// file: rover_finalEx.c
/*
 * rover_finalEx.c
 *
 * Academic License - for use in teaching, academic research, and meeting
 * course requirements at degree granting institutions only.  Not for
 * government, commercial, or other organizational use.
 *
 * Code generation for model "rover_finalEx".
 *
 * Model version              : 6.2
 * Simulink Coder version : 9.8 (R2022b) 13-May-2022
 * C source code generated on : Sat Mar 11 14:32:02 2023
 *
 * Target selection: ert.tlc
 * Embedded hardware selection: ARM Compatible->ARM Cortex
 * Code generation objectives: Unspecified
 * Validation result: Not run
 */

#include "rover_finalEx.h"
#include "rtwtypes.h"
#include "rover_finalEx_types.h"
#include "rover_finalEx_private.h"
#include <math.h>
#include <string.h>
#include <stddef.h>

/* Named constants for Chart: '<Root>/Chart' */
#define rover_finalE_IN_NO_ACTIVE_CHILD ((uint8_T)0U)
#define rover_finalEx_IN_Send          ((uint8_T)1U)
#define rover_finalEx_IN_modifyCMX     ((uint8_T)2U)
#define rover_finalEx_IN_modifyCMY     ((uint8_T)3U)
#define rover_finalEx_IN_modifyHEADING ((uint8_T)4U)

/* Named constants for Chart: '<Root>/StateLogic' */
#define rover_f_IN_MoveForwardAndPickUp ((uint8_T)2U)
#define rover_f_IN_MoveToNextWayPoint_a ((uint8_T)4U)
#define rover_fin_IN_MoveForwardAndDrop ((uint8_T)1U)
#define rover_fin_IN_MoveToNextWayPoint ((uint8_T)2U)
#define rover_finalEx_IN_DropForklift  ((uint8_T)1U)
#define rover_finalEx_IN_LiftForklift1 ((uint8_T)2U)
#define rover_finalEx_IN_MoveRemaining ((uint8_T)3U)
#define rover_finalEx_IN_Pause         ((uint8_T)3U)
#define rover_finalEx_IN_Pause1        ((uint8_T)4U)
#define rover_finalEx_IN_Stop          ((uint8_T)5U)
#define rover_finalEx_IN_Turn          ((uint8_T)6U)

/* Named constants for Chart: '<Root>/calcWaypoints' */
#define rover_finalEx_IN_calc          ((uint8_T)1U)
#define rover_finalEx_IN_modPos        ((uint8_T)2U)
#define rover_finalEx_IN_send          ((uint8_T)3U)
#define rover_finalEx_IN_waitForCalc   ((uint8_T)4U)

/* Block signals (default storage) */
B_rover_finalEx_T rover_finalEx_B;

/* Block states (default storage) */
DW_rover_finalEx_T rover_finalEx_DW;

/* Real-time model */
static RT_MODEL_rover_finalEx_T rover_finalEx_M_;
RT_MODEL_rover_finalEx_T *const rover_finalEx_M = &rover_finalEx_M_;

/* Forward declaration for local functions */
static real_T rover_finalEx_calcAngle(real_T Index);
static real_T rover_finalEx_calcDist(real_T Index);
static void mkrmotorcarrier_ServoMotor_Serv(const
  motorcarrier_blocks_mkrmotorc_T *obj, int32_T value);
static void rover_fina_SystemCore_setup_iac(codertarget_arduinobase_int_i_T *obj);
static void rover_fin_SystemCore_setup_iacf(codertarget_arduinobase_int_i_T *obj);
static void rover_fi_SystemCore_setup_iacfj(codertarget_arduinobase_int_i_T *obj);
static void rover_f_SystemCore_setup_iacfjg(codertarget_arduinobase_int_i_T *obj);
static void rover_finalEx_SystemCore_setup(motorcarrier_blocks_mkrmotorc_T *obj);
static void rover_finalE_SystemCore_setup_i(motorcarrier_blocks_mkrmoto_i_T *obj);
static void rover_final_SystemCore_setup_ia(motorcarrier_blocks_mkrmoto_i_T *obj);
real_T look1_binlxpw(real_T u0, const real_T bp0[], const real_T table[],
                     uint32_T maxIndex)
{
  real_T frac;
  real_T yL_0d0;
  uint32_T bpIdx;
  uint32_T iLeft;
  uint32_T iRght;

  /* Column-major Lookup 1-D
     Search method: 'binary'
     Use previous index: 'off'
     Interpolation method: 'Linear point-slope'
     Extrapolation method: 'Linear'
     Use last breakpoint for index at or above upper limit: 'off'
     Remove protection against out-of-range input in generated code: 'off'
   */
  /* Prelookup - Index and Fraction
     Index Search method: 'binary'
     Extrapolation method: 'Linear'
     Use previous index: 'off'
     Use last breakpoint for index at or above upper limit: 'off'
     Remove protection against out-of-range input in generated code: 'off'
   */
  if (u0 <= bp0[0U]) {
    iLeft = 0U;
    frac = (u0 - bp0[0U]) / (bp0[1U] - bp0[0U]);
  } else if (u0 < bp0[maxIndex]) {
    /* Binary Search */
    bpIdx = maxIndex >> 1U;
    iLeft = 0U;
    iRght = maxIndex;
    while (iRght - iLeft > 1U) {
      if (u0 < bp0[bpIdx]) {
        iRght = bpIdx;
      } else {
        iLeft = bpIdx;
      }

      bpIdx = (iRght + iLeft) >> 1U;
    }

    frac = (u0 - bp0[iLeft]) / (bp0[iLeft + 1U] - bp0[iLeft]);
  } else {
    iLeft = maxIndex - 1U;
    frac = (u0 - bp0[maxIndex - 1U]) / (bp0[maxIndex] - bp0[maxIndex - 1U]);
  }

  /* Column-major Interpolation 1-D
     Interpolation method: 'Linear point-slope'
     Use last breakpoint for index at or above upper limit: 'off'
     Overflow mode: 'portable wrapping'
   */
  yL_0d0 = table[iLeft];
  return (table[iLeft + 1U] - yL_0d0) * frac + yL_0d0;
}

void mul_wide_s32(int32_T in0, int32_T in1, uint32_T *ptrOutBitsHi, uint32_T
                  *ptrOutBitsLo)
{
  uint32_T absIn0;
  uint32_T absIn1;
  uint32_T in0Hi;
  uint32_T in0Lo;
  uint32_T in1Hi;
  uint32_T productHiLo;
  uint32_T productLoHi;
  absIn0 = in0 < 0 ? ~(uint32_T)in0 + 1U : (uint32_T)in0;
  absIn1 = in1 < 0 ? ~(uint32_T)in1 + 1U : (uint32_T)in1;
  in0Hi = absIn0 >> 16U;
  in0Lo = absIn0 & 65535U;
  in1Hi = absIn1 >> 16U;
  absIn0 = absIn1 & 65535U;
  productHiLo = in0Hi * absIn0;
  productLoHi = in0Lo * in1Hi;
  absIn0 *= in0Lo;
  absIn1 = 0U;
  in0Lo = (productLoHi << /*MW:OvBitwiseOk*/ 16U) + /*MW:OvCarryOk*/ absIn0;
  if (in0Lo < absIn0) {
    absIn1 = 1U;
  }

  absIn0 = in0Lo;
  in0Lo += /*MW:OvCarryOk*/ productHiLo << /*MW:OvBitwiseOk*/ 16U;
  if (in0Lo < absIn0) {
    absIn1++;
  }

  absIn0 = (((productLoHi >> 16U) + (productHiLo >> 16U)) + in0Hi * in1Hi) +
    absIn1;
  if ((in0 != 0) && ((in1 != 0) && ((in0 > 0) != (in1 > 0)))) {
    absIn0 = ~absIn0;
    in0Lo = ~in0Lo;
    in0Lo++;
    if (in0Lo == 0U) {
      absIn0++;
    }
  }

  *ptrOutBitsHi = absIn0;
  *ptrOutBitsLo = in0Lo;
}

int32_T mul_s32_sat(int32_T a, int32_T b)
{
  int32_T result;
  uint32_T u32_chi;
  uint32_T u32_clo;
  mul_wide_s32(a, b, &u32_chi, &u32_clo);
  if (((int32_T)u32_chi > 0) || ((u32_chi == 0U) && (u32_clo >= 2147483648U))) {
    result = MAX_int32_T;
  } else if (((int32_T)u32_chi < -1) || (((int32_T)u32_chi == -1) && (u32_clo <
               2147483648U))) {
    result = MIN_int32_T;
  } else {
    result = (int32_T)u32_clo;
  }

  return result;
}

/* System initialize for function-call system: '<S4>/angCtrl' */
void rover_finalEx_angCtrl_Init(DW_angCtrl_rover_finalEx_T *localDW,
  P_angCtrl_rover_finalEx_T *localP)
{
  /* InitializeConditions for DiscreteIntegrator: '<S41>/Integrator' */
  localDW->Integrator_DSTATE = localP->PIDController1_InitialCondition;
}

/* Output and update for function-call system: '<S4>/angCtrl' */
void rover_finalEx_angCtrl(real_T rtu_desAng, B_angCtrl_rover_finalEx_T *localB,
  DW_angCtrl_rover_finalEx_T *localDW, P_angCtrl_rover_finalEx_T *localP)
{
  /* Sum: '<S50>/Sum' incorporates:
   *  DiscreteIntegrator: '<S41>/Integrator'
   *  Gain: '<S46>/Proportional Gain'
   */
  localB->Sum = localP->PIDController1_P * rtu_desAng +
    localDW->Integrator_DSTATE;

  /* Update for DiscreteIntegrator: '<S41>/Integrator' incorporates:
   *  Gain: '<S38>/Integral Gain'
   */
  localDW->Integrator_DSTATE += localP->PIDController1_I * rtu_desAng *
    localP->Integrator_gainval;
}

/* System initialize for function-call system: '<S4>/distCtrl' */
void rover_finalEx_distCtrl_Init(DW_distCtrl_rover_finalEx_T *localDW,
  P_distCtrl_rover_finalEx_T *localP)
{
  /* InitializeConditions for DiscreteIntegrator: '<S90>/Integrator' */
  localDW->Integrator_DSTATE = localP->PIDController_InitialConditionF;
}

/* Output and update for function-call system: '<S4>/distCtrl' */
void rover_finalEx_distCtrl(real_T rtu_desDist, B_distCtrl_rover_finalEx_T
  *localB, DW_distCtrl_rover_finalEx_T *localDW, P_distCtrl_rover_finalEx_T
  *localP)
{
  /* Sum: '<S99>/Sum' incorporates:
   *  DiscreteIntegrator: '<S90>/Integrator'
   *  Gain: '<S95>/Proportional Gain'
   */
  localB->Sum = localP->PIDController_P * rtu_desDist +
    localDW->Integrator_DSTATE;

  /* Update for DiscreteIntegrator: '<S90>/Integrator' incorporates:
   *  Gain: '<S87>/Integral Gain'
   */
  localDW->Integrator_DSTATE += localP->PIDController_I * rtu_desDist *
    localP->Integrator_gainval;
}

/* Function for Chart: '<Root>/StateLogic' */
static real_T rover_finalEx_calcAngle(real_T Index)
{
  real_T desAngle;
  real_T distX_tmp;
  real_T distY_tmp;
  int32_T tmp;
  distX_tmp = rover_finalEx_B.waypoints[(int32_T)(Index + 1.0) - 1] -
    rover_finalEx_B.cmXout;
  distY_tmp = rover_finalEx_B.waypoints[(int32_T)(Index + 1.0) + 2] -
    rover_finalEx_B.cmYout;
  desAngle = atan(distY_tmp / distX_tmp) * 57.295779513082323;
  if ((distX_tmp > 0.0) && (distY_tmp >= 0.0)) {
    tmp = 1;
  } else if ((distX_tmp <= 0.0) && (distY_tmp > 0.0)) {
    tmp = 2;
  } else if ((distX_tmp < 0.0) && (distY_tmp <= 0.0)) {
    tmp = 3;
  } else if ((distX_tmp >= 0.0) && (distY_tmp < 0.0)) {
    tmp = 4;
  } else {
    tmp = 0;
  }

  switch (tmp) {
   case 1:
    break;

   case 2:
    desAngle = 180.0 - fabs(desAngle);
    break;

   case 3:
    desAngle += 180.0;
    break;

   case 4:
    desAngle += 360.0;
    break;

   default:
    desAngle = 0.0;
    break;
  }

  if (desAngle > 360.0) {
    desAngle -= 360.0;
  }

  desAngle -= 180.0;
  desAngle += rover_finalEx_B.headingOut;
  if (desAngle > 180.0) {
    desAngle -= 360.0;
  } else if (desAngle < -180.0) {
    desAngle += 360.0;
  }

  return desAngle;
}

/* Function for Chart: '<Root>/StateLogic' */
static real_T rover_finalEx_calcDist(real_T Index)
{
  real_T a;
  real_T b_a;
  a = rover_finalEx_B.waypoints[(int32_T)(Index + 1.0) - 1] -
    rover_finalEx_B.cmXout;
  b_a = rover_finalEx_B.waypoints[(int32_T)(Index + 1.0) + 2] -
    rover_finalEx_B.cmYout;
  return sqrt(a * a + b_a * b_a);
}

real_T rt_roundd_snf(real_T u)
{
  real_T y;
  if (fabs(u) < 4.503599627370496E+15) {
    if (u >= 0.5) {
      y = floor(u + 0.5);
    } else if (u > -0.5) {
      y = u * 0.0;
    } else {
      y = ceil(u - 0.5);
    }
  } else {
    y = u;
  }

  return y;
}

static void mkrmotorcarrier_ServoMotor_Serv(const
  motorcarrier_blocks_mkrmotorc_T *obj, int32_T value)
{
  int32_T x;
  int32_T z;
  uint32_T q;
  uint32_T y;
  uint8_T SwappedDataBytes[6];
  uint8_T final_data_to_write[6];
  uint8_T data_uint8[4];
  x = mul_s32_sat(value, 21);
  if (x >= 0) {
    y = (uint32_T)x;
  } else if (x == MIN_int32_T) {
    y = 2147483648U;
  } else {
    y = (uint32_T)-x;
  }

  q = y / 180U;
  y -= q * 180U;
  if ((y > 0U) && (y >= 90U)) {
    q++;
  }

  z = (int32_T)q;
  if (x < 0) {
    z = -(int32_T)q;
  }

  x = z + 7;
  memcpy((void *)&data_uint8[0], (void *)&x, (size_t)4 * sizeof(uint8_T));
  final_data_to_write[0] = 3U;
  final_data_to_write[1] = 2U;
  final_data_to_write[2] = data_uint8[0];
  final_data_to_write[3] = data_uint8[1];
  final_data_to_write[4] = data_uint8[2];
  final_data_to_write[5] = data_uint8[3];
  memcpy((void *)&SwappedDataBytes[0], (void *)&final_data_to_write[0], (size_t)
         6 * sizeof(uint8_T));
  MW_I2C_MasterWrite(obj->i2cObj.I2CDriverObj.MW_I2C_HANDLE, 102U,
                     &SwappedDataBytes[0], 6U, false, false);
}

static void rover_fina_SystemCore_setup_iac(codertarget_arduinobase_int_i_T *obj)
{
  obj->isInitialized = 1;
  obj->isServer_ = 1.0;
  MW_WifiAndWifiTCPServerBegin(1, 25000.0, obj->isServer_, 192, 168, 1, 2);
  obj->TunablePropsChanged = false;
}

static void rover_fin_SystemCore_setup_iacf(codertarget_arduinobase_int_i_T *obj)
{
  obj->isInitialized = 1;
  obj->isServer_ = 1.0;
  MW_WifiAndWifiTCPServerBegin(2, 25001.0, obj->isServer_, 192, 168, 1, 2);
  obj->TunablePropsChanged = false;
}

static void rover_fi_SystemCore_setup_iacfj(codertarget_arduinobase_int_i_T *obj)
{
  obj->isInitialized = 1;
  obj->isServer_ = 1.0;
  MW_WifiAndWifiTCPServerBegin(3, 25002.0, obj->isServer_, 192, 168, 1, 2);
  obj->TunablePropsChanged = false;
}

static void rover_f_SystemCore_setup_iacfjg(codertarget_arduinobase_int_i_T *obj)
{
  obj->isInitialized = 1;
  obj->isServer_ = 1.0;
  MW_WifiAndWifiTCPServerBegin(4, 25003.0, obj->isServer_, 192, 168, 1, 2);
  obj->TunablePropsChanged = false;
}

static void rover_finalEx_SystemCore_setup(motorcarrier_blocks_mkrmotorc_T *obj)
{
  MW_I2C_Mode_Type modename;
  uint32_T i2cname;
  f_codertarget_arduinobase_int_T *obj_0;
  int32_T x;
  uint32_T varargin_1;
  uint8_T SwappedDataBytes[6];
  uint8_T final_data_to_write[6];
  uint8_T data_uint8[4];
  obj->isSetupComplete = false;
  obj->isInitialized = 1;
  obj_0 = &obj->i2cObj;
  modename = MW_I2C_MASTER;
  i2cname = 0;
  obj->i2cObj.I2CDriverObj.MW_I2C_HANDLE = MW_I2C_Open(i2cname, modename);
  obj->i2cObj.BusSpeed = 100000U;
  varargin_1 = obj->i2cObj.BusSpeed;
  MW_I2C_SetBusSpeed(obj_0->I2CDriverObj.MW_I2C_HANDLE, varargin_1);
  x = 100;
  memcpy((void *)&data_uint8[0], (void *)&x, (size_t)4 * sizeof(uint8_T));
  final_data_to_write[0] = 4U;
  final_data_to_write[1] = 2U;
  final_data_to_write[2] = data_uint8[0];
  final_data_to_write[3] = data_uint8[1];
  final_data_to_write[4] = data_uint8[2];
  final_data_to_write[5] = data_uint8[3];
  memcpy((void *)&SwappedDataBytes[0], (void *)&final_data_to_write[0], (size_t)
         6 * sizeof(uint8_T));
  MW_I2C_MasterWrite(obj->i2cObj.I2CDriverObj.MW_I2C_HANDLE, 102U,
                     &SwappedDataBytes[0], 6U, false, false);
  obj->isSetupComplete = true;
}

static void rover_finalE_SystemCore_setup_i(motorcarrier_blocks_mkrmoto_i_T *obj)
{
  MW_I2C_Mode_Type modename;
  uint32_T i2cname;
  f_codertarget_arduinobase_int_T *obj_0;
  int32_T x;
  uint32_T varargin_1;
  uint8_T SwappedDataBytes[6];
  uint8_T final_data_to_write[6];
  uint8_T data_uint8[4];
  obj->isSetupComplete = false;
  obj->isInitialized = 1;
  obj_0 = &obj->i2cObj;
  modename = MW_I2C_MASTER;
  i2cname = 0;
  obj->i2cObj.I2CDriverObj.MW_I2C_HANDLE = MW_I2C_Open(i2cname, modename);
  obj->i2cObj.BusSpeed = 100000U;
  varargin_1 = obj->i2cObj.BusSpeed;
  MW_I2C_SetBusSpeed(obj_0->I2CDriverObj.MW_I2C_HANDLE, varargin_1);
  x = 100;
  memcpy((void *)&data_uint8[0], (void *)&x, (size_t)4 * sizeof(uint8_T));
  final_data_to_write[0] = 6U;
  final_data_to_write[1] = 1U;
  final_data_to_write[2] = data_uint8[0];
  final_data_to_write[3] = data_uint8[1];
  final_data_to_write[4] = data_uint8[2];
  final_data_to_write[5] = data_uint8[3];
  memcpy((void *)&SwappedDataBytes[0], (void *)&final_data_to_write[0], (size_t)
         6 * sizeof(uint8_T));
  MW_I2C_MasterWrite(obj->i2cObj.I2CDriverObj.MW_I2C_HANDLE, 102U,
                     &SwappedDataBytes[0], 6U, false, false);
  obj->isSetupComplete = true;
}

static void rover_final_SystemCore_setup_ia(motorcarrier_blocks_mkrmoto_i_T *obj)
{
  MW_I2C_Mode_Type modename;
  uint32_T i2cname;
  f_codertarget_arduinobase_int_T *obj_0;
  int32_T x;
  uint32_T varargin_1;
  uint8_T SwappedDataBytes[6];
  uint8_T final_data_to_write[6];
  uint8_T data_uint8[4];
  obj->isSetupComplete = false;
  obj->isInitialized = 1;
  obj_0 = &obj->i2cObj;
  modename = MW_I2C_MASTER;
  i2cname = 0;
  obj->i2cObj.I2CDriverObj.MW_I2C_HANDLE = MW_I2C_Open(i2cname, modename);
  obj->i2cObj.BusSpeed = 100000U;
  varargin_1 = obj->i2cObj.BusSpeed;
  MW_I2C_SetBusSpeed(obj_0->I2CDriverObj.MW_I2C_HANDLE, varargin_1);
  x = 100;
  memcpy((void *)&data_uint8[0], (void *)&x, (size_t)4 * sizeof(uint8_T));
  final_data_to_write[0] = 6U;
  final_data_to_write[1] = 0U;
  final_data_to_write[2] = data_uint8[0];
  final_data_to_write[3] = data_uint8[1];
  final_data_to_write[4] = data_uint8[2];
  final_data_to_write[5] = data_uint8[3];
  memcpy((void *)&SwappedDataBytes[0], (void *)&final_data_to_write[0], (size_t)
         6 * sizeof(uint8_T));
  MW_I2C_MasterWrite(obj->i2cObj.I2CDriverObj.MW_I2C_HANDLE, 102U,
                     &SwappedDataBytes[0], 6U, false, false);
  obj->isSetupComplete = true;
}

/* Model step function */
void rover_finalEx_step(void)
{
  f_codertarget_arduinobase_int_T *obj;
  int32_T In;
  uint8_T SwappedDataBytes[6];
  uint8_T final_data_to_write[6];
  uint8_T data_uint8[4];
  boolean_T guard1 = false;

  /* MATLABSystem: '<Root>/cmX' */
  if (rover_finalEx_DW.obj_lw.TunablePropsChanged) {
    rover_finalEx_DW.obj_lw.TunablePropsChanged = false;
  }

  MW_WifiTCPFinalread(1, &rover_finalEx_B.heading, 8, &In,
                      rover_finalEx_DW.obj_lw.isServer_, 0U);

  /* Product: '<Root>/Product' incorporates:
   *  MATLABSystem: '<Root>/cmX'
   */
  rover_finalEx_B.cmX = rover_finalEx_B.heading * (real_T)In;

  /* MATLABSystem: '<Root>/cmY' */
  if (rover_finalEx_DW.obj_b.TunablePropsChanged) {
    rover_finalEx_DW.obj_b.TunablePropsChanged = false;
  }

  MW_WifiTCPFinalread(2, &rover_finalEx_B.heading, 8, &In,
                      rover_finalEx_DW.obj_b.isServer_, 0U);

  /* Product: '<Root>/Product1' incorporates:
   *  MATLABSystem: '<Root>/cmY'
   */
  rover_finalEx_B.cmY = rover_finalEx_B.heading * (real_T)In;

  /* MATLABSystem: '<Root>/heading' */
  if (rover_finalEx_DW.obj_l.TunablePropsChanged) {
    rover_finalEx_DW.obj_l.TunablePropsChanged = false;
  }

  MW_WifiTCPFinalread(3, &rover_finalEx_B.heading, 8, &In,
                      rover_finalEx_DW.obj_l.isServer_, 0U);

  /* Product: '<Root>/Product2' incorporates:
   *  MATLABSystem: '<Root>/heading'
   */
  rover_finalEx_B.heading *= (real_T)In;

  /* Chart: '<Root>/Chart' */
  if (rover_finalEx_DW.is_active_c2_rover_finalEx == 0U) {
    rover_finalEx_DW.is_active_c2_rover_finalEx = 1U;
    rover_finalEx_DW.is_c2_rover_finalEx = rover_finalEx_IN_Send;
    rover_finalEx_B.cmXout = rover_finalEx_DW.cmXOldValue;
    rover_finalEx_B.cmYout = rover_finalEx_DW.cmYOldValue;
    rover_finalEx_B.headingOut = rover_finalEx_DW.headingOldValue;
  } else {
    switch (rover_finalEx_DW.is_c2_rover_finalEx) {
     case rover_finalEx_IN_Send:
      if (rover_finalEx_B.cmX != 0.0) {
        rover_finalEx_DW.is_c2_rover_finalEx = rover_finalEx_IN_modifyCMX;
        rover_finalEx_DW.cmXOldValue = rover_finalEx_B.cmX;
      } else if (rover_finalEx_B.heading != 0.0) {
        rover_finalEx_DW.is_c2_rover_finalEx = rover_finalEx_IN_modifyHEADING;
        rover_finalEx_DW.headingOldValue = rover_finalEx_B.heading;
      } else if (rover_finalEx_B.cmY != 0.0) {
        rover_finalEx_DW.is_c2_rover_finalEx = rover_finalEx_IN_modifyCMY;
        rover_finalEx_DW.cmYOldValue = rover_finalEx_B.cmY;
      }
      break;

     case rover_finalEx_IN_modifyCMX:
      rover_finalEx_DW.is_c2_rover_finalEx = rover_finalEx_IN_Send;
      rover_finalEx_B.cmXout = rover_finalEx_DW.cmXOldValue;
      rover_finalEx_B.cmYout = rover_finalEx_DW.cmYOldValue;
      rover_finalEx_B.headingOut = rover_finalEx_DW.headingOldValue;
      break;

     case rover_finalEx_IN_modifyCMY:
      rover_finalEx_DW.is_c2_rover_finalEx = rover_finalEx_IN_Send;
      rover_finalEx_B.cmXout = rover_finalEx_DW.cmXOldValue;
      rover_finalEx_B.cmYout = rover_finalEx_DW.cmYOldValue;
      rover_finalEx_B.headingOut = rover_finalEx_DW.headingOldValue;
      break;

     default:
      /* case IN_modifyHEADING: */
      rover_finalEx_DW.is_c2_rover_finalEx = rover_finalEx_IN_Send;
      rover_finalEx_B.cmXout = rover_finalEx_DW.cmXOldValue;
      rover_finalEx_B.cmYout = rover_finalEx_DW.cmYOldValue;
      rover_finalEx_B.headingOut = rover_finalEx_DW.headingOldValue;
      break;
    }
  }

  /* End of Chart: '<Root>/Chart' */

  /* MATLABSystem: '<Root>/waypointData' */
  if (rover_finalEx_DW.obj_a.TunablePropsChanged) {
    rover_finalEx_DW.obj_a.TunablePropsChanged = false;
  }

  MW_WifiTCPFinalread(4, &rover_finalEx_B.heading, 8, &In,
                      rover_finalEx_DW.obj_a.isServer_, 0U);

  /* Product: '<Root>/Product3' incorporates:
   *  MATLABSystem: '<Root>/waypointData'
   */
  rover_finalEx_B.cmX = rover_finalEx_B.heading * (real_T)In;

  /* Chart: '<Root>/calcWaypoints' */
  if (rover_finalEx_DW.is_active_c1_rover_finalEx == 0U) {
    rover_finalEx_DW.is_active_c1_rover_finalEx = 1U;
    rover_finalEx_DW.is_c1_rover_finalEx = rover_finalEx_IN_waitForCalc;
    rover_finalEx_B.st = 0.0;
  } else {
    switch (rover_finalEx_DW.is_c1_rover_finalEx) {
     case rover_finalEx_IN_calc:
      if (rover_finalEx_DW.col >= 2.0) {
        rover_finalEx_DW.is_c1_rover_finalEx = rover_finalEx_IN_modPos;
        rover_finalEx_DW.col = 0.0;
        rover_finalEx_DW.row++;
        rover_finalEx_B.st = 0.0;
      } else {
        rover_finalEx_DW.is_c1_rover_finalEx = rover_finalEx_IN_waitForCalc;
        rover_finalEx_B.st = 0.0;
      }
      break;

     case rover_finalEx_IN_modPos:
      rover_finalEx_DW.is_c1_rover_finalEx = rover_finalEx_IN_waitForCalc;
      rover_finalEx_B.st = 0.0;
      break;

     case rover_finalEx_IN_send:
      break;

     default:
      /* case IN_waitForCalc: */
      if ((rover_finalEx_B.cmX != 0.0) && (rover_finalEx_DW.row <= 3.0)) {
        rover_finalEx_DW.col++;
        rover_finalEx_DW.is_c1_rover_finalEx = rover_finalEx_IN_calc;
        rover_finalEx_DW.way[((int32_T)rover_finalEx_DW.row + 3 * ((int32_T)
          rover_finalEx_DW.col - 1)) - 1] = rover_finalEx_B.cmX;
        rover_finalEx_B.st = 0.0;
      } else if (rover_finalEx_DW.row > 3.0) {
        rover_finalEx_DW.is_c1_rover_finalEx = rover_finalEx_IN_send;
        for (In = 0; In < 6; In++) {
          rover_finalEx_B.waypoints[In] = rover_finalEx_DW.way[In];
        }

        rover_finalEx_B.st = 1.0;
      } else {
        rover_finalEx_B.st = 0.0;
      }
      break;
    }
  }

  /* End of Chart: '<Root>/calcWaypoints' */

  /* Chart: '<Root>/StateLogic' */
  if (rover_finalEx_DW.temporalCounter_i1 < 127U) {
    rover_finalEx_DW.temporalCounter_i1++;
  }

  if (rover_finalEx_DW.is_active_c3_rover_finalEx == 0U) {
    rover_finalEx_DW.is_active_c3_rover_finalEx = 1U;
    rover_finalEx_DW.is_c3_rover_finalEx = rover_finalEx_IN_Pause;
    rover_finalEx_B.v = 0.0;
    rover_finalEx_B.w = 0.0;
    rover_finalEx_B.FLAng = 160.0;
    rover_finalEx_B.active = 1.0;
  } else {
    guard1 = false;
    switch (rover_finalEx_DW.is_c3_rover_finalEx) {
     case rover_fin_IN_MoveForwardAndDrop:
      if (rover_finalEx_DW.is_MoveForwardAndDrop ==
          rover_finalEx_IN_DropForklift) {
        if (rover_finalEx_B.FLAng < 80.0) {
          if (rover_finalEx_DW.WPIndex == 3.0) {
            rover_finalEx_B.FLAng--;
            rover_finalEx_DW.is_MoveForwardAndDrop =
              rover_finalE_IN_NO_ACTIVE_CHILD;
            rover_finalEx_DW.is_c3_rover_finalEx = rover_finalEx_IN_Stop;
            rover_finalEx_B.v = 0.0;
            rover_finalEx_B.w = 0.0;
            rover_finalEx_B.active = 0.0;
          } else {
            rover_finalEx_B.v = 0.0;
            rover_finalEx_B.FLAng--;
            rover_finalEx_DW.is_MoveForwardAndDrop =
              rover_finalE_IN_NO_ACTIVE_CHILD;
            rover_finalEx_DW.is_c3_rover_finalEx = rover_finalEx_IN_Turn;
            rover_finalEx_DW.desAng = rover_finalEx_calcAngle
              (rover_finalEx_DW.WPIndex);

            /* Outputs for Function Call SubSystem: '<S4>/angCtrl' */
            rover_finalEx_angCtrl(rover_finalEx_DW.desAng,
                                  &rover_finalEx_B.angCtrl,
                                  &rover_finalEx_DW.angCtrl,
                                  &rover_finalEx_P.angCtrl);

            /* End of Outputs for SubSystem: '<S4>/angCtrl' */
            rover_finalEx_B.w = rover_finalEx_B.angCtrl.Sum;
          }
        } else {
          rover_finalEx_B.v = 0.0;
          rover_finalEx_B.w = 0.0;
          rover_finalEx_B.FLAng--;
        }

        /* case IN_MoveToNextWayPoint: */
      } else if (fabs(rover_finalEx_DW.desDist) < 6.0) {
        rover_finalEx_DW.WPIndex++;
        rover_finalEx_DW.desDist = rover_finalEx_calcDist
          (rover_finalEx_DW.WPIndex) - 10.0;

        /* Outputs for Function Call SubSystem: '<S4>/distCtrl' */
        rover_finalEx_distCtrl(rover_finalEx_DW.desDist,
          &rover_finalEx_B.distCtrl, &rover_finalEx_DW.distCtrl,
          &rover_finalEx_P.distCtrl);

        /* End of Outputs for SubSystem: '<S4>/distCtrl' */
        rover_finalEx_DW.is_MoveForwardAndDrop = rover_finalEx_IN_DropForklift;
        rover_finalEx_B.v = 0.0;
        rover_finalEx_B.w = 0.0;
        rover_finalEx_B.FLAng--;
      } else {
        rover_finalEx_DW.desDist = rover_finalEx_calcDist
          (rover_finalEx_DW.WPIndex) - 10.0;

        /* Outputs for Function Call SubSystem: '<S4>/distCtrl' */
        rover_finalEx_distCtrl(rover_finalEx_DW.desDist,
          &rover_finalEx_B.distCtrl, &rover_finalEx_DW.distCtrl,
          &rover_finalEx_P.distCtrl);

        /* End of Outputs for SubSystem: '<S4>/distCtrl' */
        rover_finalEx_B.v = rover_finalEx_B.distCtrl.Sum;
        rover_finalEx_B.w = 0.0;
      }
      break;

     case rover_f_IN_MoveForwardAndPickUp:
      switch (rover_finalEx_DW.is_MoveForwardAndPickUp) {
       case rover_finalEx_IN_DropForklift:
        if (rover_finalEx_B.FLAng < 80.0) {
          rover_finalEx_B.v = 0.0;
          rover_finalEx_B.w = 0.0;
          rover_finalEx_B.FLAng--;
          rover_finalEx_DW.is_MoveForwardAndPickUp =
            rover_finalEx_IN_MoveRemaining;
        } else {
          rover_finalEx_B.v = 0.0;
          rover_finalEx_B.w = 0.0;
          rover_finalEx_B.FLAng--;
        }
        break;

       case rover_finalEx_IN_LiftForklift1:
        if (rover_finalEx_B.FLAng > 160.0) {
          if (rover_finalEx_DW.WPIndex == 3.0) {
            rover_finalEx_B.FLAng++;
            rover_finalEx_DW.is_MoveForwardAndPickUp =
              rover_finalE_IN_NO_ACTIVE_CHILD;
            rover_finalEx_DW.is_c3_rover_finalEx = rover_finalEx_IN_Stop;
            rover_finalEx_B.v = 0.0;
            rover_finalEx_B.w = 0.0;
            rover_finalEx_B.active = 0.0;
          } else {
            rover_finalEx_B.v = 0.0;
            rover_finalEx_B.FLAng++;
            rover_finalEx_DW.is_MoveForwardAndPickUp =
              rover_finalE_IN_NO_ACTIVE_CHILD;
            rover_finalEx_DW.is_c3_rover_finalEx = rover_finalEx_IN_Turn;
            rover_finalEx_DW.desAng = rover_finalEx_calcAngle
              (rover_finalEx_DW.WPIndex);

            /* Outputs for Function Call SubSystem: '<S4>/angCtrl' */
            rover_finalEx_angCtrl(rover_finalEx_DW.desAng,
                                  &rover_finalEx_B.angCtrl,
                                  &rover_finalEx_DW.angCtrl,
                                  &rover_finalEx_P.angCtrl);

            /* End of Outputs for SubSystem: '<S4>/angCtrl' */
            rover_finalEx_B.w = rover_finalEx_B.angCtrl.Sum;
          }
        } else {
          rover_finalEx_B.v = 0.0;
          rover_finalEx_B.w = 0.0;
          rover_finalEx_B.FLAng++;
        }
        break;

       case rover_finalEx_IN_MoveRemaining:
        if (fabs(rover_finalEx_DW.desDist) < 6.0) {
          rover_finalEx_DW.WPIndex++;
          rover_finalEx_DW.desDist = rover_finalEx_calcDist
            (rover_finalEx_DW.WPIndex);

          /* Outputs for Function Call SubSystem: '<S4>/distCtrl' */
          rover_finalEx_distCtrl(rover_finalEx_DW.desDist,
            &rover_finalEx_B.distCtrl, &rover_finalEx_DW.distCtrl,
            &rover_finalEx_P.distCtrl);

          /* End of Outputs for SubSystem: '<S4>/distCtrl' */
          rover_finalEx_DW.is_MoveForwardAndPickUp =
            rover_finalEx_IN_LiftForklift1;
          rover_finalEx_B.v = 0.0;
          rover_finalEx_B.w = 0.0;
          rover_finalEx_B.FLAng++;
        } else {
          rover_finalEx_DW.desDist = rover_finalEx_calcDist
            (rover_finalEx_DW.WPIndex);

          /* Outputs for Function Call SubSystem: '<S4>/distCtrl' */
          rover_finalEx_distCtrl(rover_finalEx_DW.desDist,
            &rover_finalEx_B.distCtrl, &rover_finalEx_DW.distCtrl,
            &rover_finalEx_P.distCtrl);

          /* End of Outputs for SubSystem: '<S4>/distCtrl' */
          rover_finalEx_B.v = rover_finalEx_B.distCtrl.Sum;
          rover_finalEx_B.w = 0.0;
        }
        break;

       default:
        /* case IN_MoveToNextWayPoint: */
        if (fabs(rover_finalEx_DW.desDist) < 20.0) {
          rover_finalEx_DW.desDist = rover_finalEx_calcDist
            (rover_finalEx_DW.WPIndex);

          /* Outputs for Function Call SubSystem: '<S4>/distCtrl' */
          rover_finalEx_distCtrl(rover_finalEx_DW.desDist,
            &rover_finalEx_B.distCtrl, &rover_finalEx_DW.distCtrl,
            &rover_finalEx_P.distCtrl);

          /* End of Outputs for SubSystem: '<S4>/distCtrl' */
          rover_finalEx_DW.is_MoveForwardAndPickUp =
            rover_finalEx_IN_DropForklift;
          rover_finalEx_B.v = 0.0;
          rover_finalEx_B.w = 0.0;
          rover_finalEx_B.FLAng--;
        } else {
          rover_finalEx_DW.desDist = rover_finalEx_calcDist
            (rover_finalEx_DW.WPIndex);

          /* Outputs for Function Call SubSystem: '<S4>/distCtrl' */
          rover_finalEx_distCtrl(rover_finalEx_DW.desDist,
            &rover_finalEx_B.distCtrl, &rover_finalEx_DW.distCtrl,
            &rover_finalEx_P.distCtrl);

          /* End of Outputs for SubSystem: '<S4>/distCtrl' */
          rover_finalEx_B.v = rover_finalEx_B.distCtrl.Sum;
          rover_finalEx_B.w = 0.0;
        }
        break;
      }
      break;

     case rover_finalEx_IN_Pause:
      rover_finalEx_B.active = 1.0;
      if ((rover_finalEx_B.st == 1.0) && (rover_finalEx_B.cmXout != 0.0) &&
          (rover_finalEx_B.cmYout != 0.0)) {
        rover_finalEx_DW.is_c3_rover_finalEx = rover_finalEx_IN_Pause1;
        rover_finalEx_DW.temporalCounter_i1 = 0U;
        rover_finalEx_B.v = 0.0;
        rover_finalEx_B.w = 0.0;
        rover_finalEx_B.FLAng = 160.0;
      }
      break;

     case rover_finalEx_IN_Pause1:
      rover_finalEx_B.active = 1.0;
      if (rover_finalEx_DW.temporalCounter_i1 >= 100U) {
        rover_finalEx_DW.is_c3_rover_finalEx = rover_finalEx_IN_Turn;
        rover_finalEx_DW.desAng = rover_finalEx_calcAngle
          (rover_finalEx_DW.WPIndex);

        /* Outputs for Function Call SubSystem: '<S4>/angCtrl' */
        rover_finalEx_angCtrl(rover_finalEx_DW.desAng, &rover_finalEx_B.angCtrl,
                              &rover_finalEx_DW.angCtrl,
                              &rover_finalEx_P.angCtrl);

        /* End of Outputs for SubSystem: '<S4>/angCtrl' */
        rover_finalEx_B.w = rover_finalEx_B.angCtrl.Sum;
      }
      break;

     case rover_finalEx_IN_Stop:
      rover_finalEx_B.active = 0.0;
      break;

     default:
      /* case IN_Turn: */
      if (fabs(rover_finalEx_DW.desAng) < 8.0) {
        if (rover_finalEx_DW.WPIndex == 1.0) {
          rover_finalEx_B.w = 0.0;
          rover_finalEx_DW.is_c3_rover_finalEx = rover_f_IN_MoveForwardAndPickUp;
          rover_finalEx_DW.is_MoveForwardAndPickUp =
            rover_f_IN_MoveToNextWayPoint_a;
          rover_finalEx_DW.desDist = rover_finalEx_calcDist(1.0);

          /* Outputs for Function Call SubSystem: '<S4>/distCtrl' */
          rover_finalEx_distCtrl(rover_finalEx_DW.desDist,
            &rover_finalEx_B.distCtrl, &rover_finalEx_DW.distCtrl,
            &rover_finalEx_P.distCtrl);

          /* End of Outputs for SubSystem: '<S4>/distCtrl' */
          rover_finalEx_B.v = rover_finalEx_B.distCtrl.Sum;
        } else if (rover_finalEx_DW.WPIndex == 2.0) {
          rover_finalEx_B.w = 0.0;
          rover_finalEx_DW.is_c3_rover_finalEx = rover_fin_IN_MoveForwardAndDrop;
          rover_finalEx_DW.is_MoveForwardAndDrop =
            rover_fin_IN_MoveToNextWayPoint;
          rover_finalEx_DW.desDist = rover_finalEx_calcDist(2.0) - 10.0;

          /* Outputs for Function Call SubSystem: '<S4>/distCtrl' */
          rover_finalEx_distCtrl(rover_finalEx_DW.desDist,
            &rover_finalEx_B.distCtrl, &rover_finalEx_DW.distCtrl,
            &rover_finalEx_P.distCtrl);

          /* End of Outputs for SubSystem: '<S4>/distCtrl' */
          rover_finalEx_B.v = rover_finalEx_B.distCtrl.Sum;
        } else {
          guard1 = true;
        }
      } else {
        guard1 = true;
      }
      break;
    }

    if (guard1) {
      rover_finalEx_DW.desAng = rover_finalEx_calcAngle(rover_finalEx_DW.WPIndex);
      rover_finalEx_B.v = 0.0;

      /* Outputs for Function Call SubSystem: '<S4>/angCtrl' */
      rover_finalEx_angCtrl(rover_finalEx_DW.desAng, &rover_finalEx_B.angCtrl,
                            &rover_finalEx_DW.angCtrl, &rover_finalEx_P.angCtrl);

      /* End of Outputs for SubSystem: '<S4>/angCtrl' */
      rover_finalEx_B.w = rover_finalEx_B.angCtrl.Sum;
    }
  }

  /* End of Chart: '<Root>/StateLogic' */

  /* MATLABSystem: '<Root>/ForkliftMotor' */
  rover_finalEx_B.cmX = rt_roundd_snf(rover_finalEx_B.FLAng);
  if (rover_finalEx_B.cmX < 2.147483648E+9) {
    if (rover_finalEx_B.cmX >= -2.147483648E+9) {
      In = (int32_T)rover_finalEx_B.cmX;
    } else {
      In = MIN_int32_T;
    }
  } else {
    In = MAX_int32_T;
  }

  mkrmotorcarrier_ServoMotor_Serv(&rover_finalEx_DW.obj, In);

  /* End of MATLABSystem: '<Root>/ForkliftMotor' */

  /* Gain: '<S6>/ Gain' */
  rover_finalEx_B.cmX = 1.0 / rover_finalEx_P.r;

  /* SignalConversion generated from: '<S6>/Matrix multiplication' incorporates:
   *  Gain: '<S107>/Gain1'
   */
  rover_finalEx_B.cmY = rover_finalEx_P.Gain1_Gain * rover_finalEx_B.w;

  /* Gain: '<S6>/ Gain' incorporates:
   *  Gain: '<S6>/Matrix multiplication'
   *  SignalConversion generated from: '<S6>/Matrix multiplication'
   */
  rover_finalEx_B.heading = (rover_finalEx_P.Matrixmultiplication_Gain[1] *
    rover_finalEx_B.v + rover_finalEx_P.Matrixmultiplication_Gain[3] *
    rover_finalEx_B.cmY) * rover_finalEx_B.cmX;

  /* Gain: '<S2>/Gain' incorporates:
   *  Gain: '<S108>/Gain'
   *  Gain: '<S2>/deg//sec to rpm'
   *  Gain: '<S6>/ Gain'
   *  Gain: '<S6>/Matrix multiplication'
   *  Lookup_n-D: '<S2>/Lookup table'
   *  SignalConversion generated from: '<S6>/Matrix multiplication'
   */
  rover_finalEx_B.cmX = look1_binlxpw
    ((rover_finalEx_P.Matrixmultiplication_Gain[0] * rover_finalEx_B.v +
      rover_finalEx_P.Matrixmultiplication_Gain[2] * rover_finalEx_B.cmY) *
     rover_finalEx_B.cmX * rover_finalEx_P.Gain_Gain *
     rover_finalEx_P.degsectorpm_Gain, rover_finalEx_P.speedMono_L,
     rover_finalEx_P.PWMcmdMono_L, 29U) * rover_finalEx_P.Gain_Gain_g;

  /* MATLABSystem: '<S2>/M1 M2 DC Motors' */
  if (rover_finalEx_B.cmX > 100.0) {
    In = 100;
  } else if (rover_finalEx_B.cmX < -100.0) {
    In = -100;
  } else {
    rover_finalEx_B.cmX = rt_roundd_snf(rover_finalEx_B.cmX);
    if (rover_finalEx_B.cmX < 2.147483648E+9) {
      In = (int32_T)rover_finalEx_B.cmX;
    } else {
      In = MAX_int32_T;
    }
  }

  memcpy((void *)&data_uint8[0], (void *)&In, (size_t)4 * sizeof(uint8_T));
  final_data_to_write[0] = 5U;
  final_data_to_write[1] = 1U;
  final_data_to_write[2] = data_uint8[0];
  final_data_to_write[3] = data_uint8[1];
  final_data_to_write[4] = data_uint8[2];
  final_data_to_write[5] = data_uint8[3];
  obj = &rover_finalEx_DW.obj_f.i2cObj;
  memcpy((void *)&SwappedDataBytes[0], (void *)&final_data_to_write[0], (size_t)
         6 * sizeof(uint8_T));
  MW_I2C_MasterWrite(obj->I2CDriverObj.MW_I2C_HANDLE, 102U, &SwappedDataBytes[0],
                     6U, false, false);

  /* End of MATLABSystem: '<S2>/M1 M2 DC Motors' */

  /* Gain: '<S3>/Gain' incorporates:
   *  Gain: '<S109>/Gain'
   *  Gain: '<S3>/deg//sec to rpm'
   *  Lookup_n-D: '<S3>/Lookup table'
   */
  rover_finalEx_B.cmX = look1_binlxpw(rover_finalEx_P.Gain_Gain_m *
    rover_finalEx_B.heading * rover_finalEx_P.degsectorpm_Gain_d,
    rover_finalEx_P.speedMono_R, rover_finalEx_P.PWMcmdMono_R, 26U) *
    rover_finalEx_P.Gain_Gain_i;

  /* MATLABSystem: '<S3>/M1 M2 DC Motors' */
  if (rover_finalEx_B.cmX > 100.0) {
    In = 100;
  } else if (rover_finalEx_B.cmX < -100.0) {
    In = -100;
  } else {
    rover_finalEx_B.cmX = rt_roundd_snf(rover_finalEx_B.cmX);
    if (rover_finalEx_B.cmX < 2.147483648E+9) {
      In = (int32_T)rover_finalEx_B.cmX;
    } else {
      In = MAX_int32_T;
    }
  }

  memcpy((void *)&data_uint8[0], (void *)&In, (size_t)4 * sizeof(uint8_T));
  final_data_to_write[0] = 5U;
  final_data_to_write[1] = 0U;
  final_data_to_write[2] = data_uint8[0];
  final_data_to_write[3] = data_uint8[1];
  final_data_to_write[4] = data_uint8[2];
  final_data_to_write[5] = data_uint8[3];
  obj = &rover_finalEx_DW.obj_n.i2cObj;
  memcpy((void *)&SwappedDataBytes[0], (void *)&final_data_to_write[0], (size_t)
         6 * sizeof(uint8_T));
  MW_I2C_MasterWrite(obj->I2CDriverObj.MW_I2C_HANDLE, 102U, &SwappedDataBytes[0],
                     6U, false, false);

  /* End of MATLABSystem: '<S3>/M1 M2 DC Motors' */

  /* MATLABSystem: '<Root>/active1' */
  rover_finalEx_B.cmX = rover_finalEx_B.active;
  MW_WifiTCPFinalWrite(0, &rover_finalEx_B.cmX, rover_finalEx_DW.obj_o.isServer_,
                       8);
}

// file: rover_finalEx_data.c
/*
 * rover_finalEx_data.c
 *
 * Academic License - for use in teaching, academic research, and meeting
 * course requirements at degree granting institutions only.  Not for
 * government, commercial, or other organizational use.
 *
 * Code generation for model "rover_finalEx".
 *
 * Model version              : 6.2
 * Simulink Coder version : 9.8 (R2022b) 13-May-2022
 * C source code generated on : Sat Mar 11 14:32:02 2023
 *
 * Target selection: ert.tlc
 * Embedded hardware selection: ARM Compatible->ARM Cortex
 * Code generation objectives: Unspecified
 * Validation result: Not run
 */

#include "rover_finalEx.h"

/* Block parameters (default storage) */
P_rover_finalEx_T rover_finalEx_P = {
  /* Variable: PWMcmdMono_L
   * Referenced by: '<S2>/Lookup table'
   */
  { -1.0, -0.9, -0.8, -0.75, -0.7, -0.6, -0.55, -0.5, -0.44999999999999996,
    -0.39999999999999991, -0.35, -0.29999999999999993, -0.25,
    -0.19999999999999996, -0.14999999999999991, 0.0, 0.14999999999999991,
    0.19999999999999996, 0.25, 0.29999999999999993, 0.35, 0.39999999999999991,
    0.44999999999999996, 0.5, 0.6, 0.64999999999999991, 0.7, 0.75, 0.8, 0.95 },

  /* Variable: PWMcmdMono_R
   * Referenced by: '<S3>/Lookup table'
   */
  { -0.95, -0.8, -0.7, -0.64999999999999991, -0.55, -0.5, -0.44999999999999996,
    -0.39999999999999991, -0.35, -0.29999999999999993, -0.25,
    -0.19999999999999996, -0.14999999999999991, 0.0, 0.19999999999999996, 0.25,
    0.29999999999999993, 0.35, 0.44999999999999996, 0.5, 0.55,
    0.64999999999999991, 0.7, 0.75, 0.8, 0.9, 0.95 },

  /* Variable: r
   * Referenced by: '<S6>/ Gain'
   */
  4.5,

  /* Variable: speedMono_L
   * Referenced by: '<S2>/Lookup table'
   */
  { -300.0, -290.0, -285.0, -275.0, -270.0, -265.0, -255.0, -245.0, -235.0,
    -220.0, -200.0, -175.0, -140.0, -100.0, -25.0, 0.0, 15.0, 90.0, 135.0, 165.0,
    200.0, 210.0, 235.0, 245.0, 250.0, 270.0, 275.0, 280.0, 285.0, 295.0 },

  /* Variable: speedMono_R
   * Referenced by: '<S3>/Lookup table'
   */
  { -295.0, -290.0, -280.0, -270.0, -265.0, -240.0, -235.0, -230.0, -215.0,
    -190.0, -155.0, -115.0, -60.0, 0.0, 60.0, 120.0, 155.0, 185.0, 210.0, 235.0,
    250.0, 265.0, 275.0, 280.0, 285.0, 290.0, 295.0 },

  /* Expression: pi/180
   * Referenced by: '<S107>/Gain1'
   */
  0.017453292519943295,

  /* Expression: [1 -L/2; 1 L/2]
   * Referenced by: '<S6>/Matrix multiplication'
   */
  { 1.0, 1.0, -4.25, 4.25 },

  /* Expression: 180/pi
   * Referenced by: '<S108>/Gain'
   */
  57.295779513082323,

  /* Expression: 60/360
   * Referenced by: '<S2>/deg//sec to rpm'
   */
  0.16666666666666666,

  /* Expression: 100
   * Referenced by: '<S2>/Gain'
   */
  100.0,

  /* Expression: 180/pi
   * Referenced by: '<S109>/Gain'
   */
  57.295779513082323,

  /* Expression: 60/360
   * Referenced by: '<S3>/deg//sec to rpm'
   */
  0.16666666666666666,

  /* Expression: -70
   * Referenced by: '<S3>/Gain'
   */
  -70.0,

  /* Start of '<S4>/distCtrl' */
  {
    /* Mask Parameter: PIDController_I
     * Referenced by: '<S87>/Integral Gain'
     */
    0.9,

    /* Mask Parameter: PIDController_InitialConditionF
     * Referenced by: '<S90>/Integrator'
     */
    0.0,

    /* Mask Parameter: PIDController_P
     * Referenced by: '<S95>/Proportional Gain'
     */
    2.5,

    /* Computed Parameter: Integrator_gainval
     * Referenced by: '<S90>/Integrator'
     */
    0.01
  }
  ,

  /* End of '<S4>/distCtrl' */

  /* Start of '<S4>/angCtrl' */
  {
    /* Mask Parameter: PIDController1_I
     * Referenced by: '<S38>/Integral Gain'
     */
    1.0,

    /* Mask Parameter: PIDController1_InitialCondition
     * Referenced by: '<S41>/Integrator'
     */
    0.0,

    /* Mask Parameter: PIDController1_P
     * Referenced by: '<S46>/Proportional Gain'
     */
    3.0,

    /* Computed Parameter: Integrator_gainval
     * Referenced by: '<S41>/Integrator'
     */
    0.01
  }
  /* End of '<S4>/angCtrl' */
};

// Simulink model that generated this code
simulink model "rover_finalEx"  (R2022b)
settings: Solver=FixedStepAuto  StartTime=0.0  StopTime=inf  FixedStep=TS  RelTol=1e-3  EnableMultiTasking=on
PostLoadFcn:
  | paramsBasicKinematics
  | load('motorResponse.mat')
model workspace (MAT data in the model file):
  TS = 0.01
undefined symbols (not defined in the file or in its folder): L, PWMcmdMono_L, PWMcmdMono_R, r, speedMono_L, speedMono_R
libraries: arduinowifilib x5, arduinomotorcarrierlib x3, simulink_extras x3, slpidlib x2

== system rover_finalEx ==
  note: Copyright 2018 - 2020 The MathWorks, Inc.
  Chart : Stateflow chart  TreatAsAtomicUnit=on
  ForkliftMotor : arduinomotorcarrierlib/Servo Write  SlaveAddress=uint8( hex2dec( '66' ) )  blockPlatform=ARDUINO  MotorNumber=3  MotorCarrierPWMFreq=100
  LeftMotor : Subsystem
  Product{,1..3} (4 alike) : Product
  RightMotor : Subsystem
  StateLogic : Stateflow chart  TreatAsAtomicUnit=on
  active1 : arduinowifilib/WiFi TCP//IP Send  Mode_=Server  serverport=25005  RemoteAddr_=192.168.1.2  RemoteServerPort_=25005  remoteipoctet1=192  remoteipoctet2=168  remoteipoctet3=1  remoteipoctet4=2  wifiTCPServerIndex=0  wifiTCPClientIndex=0  blockPlatform=ARDUINO  isARMArch=true  SimulateUsing=Code generation
  calcWaypoints : Stateflow chart  TreatAsAtomicUnit=on
  cmX : arduinowifilib/WiFi TCP//IP Receive  Mode_=Server  serverport=25000  RemoteAddr_=192.168.1.2  RemoteServerPort_=25000  DataType_=double  DataSize_=1  SampleTime_=0.01  remoteipoctet1=192  remoteipoctet2=168  remoteipoctet3=1  remoteipoctet4=2  wifiTCPServerIndex=1  wifiTCPClientIndex=0  blockPlatform=ARDUINO  isARMArch=true  SimulateUsing=Code generation  BlockingMode_=off  BlockTimeout_=0.1
  cmY : arduinowifilib/WiFi TCP//IP Receive  Mode_=Server  serverport=25001  RemoteAddr_=192.168.1.2  RemoteServerPort_=25000  DataType_=double  DataSize_=1  SampleTime_=0.01  remoteipoctet1=192  remoteipoctet2=168  remoteipoctet3=1  remoteipoctet4=2  wifiTCPServerIndex=2  wifiTCPClientIndex=0  blockPlatform=ARDUINO  isARMArch=true  SimulateUsing=Code generation  BlockingMode_=off  BlockTimeout_=0.1
  convToWheelVel : Subsystem
  heading : arduinowifilib/WiFi TCP//IP Receive  Mode_=Server  serverport=25002  RemoteAddr_=192.168.1.2  RemoteServerPort_=25000  DataType_=double  DataSize_=1  SampleTime_=0.01  remoteipoctet1=192  remoteipoctet2=168  remoteipoctet3=1  remoteipoctet4=2  wifiTCPServerIndex=3  wifiTCPClientIndex=0  blockPlatform=ARDUINO  isARMArch=true  SimulateUsing=Code generation  BlockingMode_=off  BlockTimeout_=0.1
  waypointData : arduinowifilib/WiFi TCP//IP Receive  Mode_=Server  serverport=25003  RemoteAddr_=192.168.1.2  RemoteServerPort_=25000  DataType_=double  DataSize_=1  SampleTime_=0.01  remoteipoctet1=192  remoteipoctet2=168  remoteipoctet3=1  remoteipoctet4=2  wifiTCPServerIndex=4  wifiTCPClientIndex=0  blockPlatform=ARDUINO  isARMArch=true  SimulateUsing=Code generation  BlockingMode_=off  BlockTimeout_=0.1
  wires:
  Product3/1 -> calcWaypoints/1(waypointData)
  StateLogic/4(active) -> active1/1
  waypointData/1 -> Product3/1
  convToWheelVel/1(wl (deg/s)) -> LeftMotor/1(wl)
  convToWheelVel/2(wr (deg/s)) -> RightMotor/1(wr)
  Product2/1 -> Chart/3(heading)  "heading"
  calcWaypoints/1(waypoints) -> StateLogic/3(Waypoints)
  calcWaypoints/2(st) -> StateLogic/5(st)
  Chart/1(cmXout) -> StateLogic/1(cmX)
  Chart/3(headingOut) -> StateLogic/2(heading)
  Chart/2(cmYout) -> StateLogic/4(cmY)
  StateLogic/1(v) -> convToWheelVel/1(v)
  StateLogic/3(FLAng) -> ForkliftMotor/1
  heading/2 -> Product2/2
  heading/1 -> Product2/1
  cmX/1 -> Product/1
  Product1/1 -> Chart/2(cmY)  "cmY"
  cmX/2 -> Product/2
  Product/1 -> Chart/1(cmX)  "cmX"
  StateLogic/2(w) -> convToWheelVel/2(w)
  waypointData/2 -> Product3/2
  cmY/2 -> Product1/2
  cmY/1 -> Product1/1

== system rover_finalEx/LeftMotor ==
  wl : Inport
  Gain : Gain  Gain=100
  Lookup table : Lookup_n-D  NumberOfTableDimensions=1  BreakpointsForDimension1=speedMono_L  Table=PWMcmdMono_L  UseLastTableValue=on  InternalRulePriority=Speed  RndMeth=Simplest
  M1 M2 DC Motors : arduinomotorcarrierlib/M1 M2 DC Motors  SlaveAddress=uint8( hex2dec( '66' ) )  blockPlatform=ARDUINO  MotorNumber=M2  MotorCarrierPWMFreq=100
  deg/sec to rpm : Gain  Gain=60/360
  wires:
  wl/1 -> deg/sec to rpm/1  "desired"
  Lookup table/1 -> Gain/1  "commanded"
  Gain/1 -> M1 M2 DC Motors/1
  deg/sec to rpm/1 -> Lookup table/1

== system rover_finalEx/RightMotor ==
  wr : Inport
  Gain : Gain  Gain=-70
  Lookup table : Lookup_n-D  NumberOfTableDimensions=1  BreakpointsForDimension1=speedMono_R  Table=PWMcmdMono_R  UseLastTableValue=on  InternalRulePriority=Speed  RndMeth=Simplest
  M1 M2 DC Motors : arduinomotorcarrierlib/M1 M2 DC Motors  SlaveAddress=uint8( hex2dec( '66' ) )  blockPlatform=ARDUINO  MotorNumber=M1  MotorCarrierPWMFreq=100
  deg/sec to rpm : Gain  Gain=60/360
  wires:
  wr/1 -> deg/sec to rpm/1  "desired"
  Lookup table/1 -> Gain/1  "commanded"
  Gain/1 -> M1 M2 DC Motors/1
  deg/sec to rpm/1 -> Lookup table/1

== system rover_finalEx/StateLogic/angCtrl ==
  desAng : Inport  OutDataTypeStr=double  PortDimensions=1
  f : TriggerPort  TriggerType=function-call  VariantControl=(inherit)  PropagateVarSize=Only when enabling  SampleTimeType=periodic  SampleTime=TS
  PID Controller1 : slpidlib/PID Controller  Controller=PI  Form=Parallel  TimeDomain=Discrete-time  UseExternalTs=off  SampleTime=-1  IntegratorMethod=Forward Euler  FilterMethod=Forward Euler  ControllerParametersSource=internal  P=3  I=1  UseKiTs=off  D=0  N=100  UseFilter=on  TunerSelectOption=Transfer Function Based (PID Tuner App)  InitialConditionSource=internal  InitialConditionForIntegrator=0  InitialConditionForFilter=0  DifferentiatorICPrevScaledInput=0  ExternalReset=none  TrackingMode=off  Kt=1  LimitOutput=off  SatLimitsSource=internal  UpperSaturationLimit=inf  LowerSaturationLimit=-inf  LinearizeAsGain=on  AntiWindupMode=none  Kb=1  LimitIntegrator=off  UpperIntegratorSaturationLimit=inf  LowerIntegratorSaturationLimit=-inf  POutMin=[]  POutMax=[]  IOutMin=[]  IOutMax=[]  DOutMin=[]  DOutMax=[]  NOutMin=[]  NOutMax=[]  SumOutMin=[]  SumOutMax=[]  SaturationOutMin=[]  SaturationOutMax=[]  PParamMin=[]  PParamMax=[]  IParamMin=[]  IParamMax=[]  DParamMin=[]  DParamMax=[]  NParamMin=[]  NParamMax=[]  KbParamMin=[]  KbParamMax=[]  KtParamMin=[]  KtParamMax=[]  KbOutMin=[]  KbOutMax=[]  KtOutMin=[]  KtOutMax=[]  IntegratorOutMin=[]  IntegratorOutMax=[]  FilterOutMin=[]  FilterOutMax=[]  SumI1OutMin=[]  SumI1OutMax=[]  SumI2OutMin=[]  SumI2OutMax=[]  SumI3OutMin=[]  SumI3OutMax=[]  SumI4OutMin=[]  SumI4OutMax=[]  SumDOutMin=[]  SumDOutMax=[]  DifferentiatorOutMin=[]  DifferentiatorOutMax=[]  FilterDiffOutCoefMin=[]  FilterDiffOutCoefMax=[]  ReciprocalOutMin=[]  ReciprocalOutMax=[]  SumDenOutMin=[]  SumDenOutMax=[]  SumNumOutMin=[]  SumNumOutMax=[]  DivideOutMin=[]  DivideOutMax=[]  UdiffTsProdOutMin=[]  UdiffTsProdOutMax=[]  NTsProdOutMin=[]  NTsProdOutMax=[]  UintegralTsProdOutMin=[]  UintegralTsProdOutMax=[]  UngainTsProdOutMin=[]  UngainTsProdOutMax=[]  ClampingZeroOutDataTypeStr=Inherit: Inherit via back propagation  ClampingZeroOutMin=[]  ClampingZeroOutMax=[]  FilterDenConstantOutDataTypeStr=Inherit: Inherit via back propagation  FilterDenConstantOutMin=[]  FilterDenConstantOutMax=[]  PCopyOutDataTypeStr=Inherit: Inherit via back propagation  PCopyOutMin=[]  PCopyOutMax=[]  NCopyOutDataTypeStr=Inherit: Inherit via back propagation  NCopyOutMin=[]  NCopyOutMax=[]  IntegratorContinuousStateAttributes=''  IntegratorStateMustResolveToSignalObject=off  IntegratorRTWStateStorageClass=Auto  FilterContinuousStateAttributes=''  FilterStateMustResolveToSignalObject=off  FilterRTWStateStorageClass=Auto  ParallelPVariant=InternalParameters  IdealPVariant=Disabled  IVariant=InternalParameters  DVariant=Disabled  IntegratorVariant=Discrete  SatVariant=Disabled  AWVariant=Passthrough  PCopyVariant=Disabled  TRVariant=Disabled  FdbkBlocksVariant=Forward  IdealPFdbkVariant=Disabled  SatFdbkVariant=Disabled  DerivativeFilterVariant=Disabled  NVariant=Disabled  NCopyVariant=Disabled_SignalSpec  FilterICVariant=Disabled  IntegratorICVariant=InternalICs  ExternalResetVariant=Disabled  TRSumVariant=Passthrough  SumFdbkVariant=Disabled  SumVariant=Sum_PI  TsampFilterVariant=InternalTs  TsampNgainVariant=Passthrough  TsampIntegralVariant=Passthrough  ExternalSaturationOutDataTypeStr=Inherit: Same as second input
  Scope : Scope
  w : Outport  VectorParamsAs1DForOutWhenUnconnected=off
  wires:
  desAng/1 -> Scope/1, PID Controller1/1  "desiredAng"
  PID Controller1/1 -> w/1  "w"

== system rover_finalEx/StateLogic/distCtrl ==
  desDist : Inport  OutDataTypeStr=double  PortDimensions=1
  f : TriggerPort  TriggerType=function-call  VariantControl=(inherit)  PropagateVarSize=Only when enabling  SampleTimeType=periodic  SampleTime=TS
  PID Controller : slpidlib/PID Controller  Controller=PI  Form=Parallel  TimeDomain=Discrete-time  UseExternalTs=off  SampleTime=-1  IntegratorMethod=Forward Euler  FilterMethod=Forward Euler  ControllerParametersSource=internal  P=2.5  I=0.9  UseKiTs=off  D=0  N=100  UseFilter=on  TunerSelectOption=Transfer Function Based (PID Tuner App)  InitialConditionSource=internal  InitialConditionForIntegrator=0  InitialConditionForFilter=0  DifferentiatorICPrevScaledInput=0  ExternalReset=none  TrackingMode=off  Kt=1  LimitOutput=off  SatLimitsSource=internal  UpperSaturationLimit=inf  LowerSaturationLimit=-inf  LinearizeAsGain=on  AntiWindupMode=none  Kb=1  LimitIntegrator=off  UpperIntegratorSaturationLimit=inf  LowerIntegratorSaturationLimit=-inf  POutMin=[]  POutMax=[]  IOutMin=[]  IOutMax=[]  DOutMin=[]  DOutMax=[]  NOutMin=[]  NOutMax=[]  SumOutMin=[]  SumOutMax=[]  SaturationOutMin=[]  SaturationOutMax=[]  PParamMin=[]  PParamMax=[]  IParamMin=[]  IParamMax=[]  DParamMin=[]  DParamMax=[]  NParamMin=[]  NParamMax=[]  KbParamMin=[]  KbParamMax=[]  KtParamMin=[]  KtParamMax=[]  KbOutMin=[]  KbOutMax=[]  KtOutMin=[]  KtOutMax=[]  IntegratorOutMin=[]  IntegratorOutMax=[]  FilterOutMin=[]  FilterOutMax=[]  SumI1OutMin=[]  SumI1OutMax=[]  SumI2OutMin=[]  SumI2OutMax=[]  SumI3OutMin=[]  SumI3OutMax=[]  SumI4OutMin=[]  SumI4OutMax=[]  SumDOutMin=[]  SumDOutMax=[]  DifferentiatorOutMin=[]  DifferentiatorOutMax=[]  FilterDiffOutCoefMin=[]  FilterDiffOutCoefMax=[]  ReciprocalOutMin=[]  ReciprocalOutMax=[]  SumDenOutMin=[]  SumDenOutMax=[]  SumNumOutMin=[]  SumNumOutMax=[]  DivideOutMin=[]  DivideOutMax=[]  UdiffTsProdOutMin=[]  UdiffTsProdOutMax=[]  NTsProdOutMin=[]  NTsProdOutMax=[]  UintegralTsProdOutMin=[]  UintegralTsProdOutMax=[]  UngainTsProdOutMin=[]  UngainTsProdOutMax=[]  ClampingZeroOutDataTypeStr=Inherit: Inherit via back propagation  ClampingZeroOutMin=[]  ClampingZeroOutMax=[]  FilterDenConstantOutDataTypeStr=Inherit: Inherit via back propagation  FilterDenConstantOutMin=[]  FilterDenConstantOutMax=[]  PCopyOutDataTypeStr=Inherit: Inherit via back propagation  PCopyOutMin=[]  PCopyOutMax=[]  NCopyOutDataTypeStr=Inherit: Inherit via back propagation  NCopyOutMin=[]  NCopyOutMax=[]  IntegratorContinuousStateAttributes=''  IntegratorStateMustResolveToSignalObject=off  IntegratorRTWStateStorageClass=Auto  FilterContinuousStateAttributes=''  FilterStateMustResolveToSignalObject=off  FilterRTWStateStorageClass=Auto  ParallelPVariant=InternalParameters  IdealPVariant=Disabled  IVariant=InternalParameters  DVariant=Disabled  IntegratorVariant=Discrete  SatVariant=Disabled  AWVariant=Passthrough  PCopyVariant=Disabled  TRVariant=Disabled  FdbkBlocksVariant=Forward  IdealPFdbkVariant=Disabled  SatFdbkVariant=Disabled  DerivativeFilterVariant=Disabled  NVariant=Disabled  NCopyVariant=Disabled_SignalSpec  FilterICVariant=Disabled  IntegratorICVariant=InternalICs  ExternalResetVariant=Disabled  TRSumVariant=Passthrough  SumFdbkVariant=Disabled  SumVariant=Sum_PI  TsampFilterVariant=InternalTs  TsampNgainVariant=Passthrough  TsampIntegralVariant=Passthrough  ExternalSaturationOutDataTypeStr=Inherit: Same as second input
  Scope : Scope
  v : Outport  VectorParamsAs1DForOutWhenUnconnected=off
  wires:
  desDist/1 -> Scope/1, PID Controller/1  "desiredDist"
  PID Controller/1 -> v/1  "v"

== system rover_finalEx/convToWheelVel ==
  v : Inport
  w : Inport  Port=2
  " Gain" : Gain  Gain=1/r  Multiplication=Matrix(K*u)
  Degrees to Radians : simulink_extras/Transformations/Degrees to Radians
  Demux : Demux  Outputs=2
  Matrix multiplication : Gain  Gain=[1 -L/2; 1 L/2]  Multiplication=Matrix(K*u)
  Mux : Mux  Inputs=2
  Radians to Degrees : simulink_extras/Transformations/Radians to Degrees
  Radians to Degrees1 : simulink_extras/Transformations/Radians to Degrees
  wl (deg/s) : Outport  VectorParamsAs1DForOutWhenUnconnected=off
  wr (deg/s) : Outport  Port=2  VectorParamsAs1DForOutWhenUnconnected=off
  wires:
  " Gain"/1 -> Demux/1
  Matrix multiplication/1 -> " Gain"/1
  v/1 -> Mux/1
  Mux/1 -> Matrix multiplication/1
  Demux/1 -> Radians to Degrees/1
  Demux/2 -> Radians to Degrees1/1
  w/1 -> Degrees to Radians/1
  Radians to Degrees/1 -> wl (deg/s)/1
  Radians to Degrees1/1 -> wr (deg/s)/1
  Degrees to Radians/1 -> Mux/2

== stateflow chart rover_finalEx/calcWaypoints ==
  state waitForCalc
    en, du, ex:
    st = 0;
  state send
    en:
    waypoints = way;
    st = 1;
  state calc
    en:
    way(row, col) = waypointData;
    st = 0;
  state modPos
    en:
    col = 0;
    row = row + 1;
    st = 0;
  (default) -> waitForCalc
  waitForCalc -> send [order 2] : [row > 3]
  modPos -> waitForCalc
  calc -> waitForCalc [order 2]
  waitForCalc -> calc [order 1] : [waypointData ~= 0 && (row <= 3)]{col = col+1}
  calc -> modPos [order 1] : [col >= 2]
  data: waypoints output; waypointData input; row local =1; col local =0; way local =[0 0; 0 0; 0 0]; st output

== stateflow chart rover_finalEx/Chart ==
  state modifyHEADING
    en:
    headingOldValue = heading;
  state Send
    en:
    cmXout = cmXOldValue;
    cmYout = cmYOldValue;
    headingOut = headingOldValue;
  state modifyCMX
    en:
    cmXOldValue = cmX;
  state modifyCMY
    en:
    cmYOldValue = cmY;
  (default) -> Send
  modifyHEADING -> Send
  Send -> modifyCMX [order 1] : [cmX ~= 0]
  Send -> modifyHEADING [order 2] : [heading ~= 0]
  modifyCMX -> Send
  modifyCMY -> Send
  Send -> modifyCMY [order 3] : [cmY ~= 0]
  data: cmX input; cmY input; heading input; cmXout output; cmYout output; headingOut output; cmXOldValue local =0; cmYOldValue local =0; headingOldValue local =0

== stateflow chart rover_finalEx/StateLogic ==
  state Pause
    entry:
    v = 0; w= 0; FLAng = 160;
    active = 1;
  state Pause1
    entry:
    v = 0; w = 0; FLAng = 160;
    active = 1;
  state MoveForwardAndDrop
    state MoveToNextWayPoint
      en:
      desDist = calcDist(WPIndex)-10;
      v = distCtrl(desDist);
      du, ex:
      desDist = calcDist(WPIndex)-10;
      v = distCtrl(desDist);
      w = 0;
    state DropForklift
      en, du, ex:
      v = 0;
      w = 0;
      FLAng = FLAng-1;
    (default) -> MoveForwardAndDrop.MoveToNextWayPoint
    MoveForwardAndDrop.MoveToNextWayPoint -> MoveForwardAndDrop.DropForklift : [abs(desDist) < 6]{WPIndex = WPIndex+1}
  state Turn
    en:
    desAng = calcAngle(WPIndex);
    w = angCtrl(desAng);
    du:
    desAng = calcAngle(WPIndex);
    v = 0;
    w = angCtrl(desAng);
    ex:
    w = 0;
  state w = angCtrl(desAng) [function]
  state MoveForwardAndPickUp
    state MoveToNextWayPoint
      en:
      desDist = calcDist(WPIndex);
      v = distCtrl(desDist);
      du, ex:
      desDist = calcDist(WPIndex);
      v = distCtrl(desDist);
      w = 0;
    state DropForklift
      en, du, ex:
      v = 0;
      w = 0;
      FLAng = FLAng-1;
    state MoveRemaining
      du, ex:
      desDist = calcDist(WPIndex);
      v = distCtrl(desDist);
      w = 0;
    state LiftForklift1
      en, du, ex:
      v = 0;
      w = 0;
      FLAng = FLAng+1;
    (default) -> MoveForwardAndPickUp.MoveToNextWayPoint
    MoveForwardAndPickUp.MoveToNextWayPoint -> MoveForwardAndPickUp.DropForklift : [abs(desDist) < 20]
    MoveForwardAndPickUp.DropForklift -> MoveRemaining : [FLAng < 80]
    MoveRemaining -> LiftForklift1 : [abs(desDist) < 6]{WPIndex = WPIndex+1}
  state v = distCtrl(desDist) [function]
  state Stop
    en:
    v = 0;
    w = 0;
    active = 0;
  MoveForwardAndDrop.DropForklift -> (junction 182) : [FLAng < 80]
  LiftForklift1 -> (junction 182) : [FLAng > 160]
  (default) -> Pause
  Pause -> Pause1 : [st == 1 && cmX ~= 0 && cmY ~= 0]
  Pause1 -> Turn : after(1,sec)
  Turn -> (junction 198) : [abs(desAng) < 8]
  (junction 198) -> MoveForwardAndDrop [order 2] : [WPIndex == 2]
  (junction 198) -> MoveForwardAndPickUp [order 1] : [WPIndex == 1]
  (junction 182) -> Turn [order 2]
  (junction 182) -> Stop [order 1] : [WPIndex == size(Waypoints,1)]
  data: desAngle function_output; Index function_input; desDistance function_output; Index function_input; desAng function_input double size=1; w function_output; desDist function_input double size=1; v function_output; cmX input; heading input; v output double size=1; w output double size=1; desDist local; desAng local; Waypoints input; WPIndex local =1; FLAng output; cmY input; st input; active output
  function desAngle  = calcAngle(Index):
    | function desAngle  = calcAngle(Index)
    | 
    | toReachX = Waypoints(Index+1,1);
    | toReachY = Waypoints(Index+1,2);
    | x = cmX;
    | y = cmY;
    | distX = toReachX - x;
    | distY = toReachY - y;
    | if distX > 0 && distY >= 0
    |     quadrant = 1;
    | elseif distX <= 0 && distY > 0
    |     quadrant = 2;
    | elseif distX < 0 && distY <= 0
    |     quadrant = 3;
    | elseif distX >= 0 && distY < 0
    |     quadrant = 4;
    | else
    |     quadrant = 0;
    | end
    | desAngle = atand((toReachY-y)/(toReachX-x));
    | switch quadrant
    |     case 1
    |         
    |     case 2
    |         desAngle = 180-abs(desAngle);
    |     case 3
    |         desAngle = 180+desAngle;
    |     case 4
    |         desAngle = 360+desAngle;
    |     otherwise 
    |         desAngle = 0;
    | end
    | if desAngle > 360 
    |     desAngle = desAngle - 360;
    | end
    | 
    | desAngle = desAngle - 180;      %conversion needed to avoid the offset of 
    |                                 %the value compared to heading
    | desAngle = desAngle + heading;  %the angle to face the target
    | 
    |  if(desAngle > 180)             %conversions to avoid spinning too much
    |    desAngle = desAngle - 360;
    |  elseif(desAngle < -180)
    |      desAngle = desAngle + 360;
    |  end
    | end
  function desDistance = calcDist(Index):
    | function desDistance = calcDist(Index)
    | 
    | toReachX = Waypoints(Index+1,1);
    | toReachY = Waypoints(Index+1,2);
    | x = cmX;
    | y = cmY;
    | distX = toReachX - x;
    | distY = toReachY - y;
    | desDistance = sqrt(distX^2+distY^2);
    | end
